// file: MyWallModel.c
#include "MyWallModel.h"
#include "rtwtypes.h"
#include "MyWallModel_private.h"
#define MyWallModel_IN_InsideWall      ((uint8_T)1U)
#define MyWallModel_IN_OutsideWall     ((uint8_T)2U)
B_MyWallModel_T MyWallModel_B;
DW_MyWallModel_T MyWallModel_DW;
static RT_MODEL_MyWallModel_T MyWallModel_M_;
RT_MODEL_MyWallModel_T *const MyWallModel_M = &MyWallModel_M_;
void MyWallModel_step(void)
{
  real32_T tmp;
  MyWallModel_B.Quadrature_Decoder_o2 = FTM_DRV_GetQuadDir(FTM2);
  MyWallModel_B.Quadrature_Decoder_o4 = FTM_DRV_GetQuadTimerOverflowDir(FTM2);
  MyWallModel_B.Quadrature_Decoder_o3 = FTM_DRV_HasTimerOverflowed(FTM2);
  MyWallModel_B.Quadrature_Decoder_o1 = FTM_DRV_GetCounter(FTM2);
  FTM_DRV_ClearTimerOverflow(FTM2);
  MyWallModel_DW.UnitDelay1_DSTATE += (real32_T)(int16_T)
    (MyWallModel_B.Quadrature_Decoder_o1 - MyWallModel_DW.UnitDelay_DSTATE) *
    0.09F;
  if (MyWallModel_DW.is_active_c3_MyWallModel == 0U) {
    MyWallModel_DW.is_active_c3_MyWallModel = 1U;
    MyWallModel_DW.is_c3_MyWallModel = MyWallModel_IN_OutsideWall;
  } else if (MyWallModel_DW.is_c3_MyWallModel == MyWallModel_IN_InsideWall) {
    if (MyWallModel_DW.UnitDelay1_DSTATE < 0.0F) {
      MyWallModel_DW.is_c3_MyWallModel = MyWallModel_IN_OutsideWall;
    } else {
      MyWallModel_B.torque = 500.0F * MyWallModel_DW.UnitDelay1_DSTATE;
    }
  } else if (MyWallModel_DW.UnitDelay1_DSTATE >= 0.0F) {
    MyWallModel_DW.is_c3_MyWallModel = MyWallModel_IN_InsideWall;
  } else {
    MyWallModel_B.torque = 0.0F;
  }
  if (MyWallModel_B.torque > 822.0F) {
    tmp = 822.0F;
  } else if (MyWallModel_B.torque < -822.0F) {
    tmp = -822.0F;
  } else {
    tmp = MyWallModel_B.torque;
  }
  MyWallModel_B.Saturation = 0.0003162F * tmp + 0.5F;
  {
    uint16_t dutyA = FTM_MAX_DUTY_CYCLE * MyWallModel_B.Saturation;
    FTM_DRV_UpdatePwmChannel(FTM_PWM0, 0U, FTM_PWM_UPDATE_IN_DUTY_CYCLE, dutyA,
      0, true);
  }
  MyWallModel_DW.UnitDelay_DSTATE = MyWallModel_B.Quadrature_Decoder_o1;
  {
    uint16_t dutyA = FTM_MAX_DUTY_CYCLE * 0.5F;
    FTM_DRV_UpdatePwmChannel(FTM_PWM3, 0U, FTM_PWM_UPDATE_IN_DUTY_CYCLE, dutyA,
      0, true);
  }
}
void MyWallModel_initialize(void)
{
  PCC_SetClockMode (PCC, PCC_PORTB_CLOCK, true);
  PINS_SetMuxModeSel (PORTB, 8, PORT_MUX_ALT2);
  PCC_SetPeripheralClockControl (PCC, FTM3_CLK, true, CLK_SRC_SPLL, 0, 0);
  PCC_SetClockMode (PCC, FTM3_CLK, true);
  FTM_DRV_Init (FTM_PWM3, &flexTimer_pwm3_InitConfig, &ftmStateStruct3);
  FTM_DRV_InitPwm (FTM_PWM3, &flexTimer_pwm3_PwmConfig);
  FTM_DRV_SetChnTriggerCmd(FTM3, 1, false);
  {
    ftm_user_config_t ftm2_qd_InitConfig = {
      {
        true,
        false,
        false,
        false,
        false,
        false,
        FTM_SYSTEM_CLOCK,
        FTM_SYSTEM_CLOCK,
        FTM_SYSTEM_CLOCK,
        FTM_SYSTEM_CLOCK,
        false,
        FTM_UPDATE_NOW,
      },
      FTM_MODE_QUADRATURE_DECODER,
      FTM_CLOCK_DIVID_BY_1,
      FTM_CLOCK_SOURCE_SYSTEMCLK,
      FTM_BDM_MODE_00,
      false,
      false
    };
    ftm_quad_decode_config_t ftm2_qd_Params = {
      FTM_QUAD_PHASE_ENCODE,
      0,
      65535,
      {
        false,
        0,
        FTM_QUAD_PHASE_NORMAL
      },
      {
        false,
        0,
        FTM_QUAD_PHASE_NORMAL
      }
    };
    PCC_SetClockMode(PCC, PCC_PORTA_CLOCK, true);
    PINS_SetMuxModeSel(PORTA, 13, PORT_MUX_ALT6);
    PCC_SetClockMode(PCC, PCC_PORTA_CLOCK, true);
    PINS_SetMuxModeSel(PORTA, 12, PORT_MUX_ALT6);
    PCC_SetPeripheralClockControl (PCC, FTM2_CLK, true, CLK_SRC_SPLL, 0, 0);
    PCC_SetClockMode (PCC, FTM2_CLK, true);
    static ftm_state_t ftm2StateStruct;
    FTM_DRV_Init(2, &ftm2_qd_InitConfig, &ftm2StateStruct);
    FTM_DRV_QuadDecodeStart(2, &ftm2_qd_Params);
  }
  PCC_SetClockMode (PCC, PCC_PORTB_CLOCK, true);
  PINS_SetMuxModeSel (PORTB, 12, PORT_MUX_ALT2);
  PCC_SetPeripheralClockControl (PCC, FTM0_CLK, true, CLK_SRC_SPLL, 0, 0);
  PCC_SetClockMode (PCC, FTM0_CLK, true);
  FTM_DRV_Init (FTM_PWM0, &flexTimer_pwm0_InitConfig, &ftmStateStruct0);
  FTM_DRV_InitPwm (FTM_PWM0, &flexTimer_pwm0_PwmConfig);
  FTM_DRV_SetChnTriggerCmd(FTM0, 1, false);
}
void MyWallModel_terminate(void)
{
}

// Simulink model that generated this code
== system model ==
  Subsystem#1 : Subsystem  <- Trigger: FunctionCallGenerator#1
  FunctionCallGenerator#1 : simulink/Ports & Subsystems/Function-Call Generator
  FTM_PWM_Config#1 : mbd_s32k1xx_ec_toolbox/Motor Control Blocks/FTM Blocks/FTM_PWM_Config  <- 1: Constant#1
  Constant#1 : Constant  Value=.5
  MBD_S32K1xx_Config_Information#1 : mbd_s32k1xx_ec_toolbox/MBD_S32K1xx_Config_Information
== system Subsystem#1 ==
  TriggerPort#1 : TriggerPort  TriggerType=function-call
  FTM_PWM_Config#2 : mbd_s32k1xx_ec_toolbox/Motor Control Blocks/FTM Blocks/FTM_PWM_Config  <- 1: Saturation
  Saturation : Saturate  UpperLimit=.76  LowerLimit=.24  <- 1: Sum#1
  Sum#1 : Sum  Inputs=++  <- 1: Gain#1, 2: Constant#2
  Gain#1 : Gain  Gain=3.162e-4  <- 1: Saturate#1
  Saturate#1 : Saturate  UpperLimit=822  LowerLimit=-822  <- 1: Stateflowchart#1
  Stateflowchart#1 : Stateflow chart  <- 1: Sum#2
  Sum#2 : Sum  Inputs=++  <- 1: Gain#2, 2: UnitDelay1
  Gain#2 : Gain  Gain=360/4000  <- 1: DataTypeConversion#1
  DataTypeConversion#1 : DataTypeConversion  <- 1: DataTypeConversion#2
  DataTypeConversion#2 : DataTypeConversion  <- 1: Sum#3
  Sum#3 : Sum  Inputs=+-  <- 1: DataTypeConversion#3, 2: UnitDelay
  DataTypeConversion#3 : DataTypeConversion  <- 1: Quadrature_Decoder
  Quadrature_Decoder : mbd_s32k1xx_ec_toolbox/Motor Control Blocks/FTM Blocks/Quadrature_Decoder
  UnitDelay : UnitDelay  <- 1: DataTypeConversion#3
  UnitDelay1 : UnitDelay  <- 1: Sum#2
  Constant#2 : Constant  Value=.5

